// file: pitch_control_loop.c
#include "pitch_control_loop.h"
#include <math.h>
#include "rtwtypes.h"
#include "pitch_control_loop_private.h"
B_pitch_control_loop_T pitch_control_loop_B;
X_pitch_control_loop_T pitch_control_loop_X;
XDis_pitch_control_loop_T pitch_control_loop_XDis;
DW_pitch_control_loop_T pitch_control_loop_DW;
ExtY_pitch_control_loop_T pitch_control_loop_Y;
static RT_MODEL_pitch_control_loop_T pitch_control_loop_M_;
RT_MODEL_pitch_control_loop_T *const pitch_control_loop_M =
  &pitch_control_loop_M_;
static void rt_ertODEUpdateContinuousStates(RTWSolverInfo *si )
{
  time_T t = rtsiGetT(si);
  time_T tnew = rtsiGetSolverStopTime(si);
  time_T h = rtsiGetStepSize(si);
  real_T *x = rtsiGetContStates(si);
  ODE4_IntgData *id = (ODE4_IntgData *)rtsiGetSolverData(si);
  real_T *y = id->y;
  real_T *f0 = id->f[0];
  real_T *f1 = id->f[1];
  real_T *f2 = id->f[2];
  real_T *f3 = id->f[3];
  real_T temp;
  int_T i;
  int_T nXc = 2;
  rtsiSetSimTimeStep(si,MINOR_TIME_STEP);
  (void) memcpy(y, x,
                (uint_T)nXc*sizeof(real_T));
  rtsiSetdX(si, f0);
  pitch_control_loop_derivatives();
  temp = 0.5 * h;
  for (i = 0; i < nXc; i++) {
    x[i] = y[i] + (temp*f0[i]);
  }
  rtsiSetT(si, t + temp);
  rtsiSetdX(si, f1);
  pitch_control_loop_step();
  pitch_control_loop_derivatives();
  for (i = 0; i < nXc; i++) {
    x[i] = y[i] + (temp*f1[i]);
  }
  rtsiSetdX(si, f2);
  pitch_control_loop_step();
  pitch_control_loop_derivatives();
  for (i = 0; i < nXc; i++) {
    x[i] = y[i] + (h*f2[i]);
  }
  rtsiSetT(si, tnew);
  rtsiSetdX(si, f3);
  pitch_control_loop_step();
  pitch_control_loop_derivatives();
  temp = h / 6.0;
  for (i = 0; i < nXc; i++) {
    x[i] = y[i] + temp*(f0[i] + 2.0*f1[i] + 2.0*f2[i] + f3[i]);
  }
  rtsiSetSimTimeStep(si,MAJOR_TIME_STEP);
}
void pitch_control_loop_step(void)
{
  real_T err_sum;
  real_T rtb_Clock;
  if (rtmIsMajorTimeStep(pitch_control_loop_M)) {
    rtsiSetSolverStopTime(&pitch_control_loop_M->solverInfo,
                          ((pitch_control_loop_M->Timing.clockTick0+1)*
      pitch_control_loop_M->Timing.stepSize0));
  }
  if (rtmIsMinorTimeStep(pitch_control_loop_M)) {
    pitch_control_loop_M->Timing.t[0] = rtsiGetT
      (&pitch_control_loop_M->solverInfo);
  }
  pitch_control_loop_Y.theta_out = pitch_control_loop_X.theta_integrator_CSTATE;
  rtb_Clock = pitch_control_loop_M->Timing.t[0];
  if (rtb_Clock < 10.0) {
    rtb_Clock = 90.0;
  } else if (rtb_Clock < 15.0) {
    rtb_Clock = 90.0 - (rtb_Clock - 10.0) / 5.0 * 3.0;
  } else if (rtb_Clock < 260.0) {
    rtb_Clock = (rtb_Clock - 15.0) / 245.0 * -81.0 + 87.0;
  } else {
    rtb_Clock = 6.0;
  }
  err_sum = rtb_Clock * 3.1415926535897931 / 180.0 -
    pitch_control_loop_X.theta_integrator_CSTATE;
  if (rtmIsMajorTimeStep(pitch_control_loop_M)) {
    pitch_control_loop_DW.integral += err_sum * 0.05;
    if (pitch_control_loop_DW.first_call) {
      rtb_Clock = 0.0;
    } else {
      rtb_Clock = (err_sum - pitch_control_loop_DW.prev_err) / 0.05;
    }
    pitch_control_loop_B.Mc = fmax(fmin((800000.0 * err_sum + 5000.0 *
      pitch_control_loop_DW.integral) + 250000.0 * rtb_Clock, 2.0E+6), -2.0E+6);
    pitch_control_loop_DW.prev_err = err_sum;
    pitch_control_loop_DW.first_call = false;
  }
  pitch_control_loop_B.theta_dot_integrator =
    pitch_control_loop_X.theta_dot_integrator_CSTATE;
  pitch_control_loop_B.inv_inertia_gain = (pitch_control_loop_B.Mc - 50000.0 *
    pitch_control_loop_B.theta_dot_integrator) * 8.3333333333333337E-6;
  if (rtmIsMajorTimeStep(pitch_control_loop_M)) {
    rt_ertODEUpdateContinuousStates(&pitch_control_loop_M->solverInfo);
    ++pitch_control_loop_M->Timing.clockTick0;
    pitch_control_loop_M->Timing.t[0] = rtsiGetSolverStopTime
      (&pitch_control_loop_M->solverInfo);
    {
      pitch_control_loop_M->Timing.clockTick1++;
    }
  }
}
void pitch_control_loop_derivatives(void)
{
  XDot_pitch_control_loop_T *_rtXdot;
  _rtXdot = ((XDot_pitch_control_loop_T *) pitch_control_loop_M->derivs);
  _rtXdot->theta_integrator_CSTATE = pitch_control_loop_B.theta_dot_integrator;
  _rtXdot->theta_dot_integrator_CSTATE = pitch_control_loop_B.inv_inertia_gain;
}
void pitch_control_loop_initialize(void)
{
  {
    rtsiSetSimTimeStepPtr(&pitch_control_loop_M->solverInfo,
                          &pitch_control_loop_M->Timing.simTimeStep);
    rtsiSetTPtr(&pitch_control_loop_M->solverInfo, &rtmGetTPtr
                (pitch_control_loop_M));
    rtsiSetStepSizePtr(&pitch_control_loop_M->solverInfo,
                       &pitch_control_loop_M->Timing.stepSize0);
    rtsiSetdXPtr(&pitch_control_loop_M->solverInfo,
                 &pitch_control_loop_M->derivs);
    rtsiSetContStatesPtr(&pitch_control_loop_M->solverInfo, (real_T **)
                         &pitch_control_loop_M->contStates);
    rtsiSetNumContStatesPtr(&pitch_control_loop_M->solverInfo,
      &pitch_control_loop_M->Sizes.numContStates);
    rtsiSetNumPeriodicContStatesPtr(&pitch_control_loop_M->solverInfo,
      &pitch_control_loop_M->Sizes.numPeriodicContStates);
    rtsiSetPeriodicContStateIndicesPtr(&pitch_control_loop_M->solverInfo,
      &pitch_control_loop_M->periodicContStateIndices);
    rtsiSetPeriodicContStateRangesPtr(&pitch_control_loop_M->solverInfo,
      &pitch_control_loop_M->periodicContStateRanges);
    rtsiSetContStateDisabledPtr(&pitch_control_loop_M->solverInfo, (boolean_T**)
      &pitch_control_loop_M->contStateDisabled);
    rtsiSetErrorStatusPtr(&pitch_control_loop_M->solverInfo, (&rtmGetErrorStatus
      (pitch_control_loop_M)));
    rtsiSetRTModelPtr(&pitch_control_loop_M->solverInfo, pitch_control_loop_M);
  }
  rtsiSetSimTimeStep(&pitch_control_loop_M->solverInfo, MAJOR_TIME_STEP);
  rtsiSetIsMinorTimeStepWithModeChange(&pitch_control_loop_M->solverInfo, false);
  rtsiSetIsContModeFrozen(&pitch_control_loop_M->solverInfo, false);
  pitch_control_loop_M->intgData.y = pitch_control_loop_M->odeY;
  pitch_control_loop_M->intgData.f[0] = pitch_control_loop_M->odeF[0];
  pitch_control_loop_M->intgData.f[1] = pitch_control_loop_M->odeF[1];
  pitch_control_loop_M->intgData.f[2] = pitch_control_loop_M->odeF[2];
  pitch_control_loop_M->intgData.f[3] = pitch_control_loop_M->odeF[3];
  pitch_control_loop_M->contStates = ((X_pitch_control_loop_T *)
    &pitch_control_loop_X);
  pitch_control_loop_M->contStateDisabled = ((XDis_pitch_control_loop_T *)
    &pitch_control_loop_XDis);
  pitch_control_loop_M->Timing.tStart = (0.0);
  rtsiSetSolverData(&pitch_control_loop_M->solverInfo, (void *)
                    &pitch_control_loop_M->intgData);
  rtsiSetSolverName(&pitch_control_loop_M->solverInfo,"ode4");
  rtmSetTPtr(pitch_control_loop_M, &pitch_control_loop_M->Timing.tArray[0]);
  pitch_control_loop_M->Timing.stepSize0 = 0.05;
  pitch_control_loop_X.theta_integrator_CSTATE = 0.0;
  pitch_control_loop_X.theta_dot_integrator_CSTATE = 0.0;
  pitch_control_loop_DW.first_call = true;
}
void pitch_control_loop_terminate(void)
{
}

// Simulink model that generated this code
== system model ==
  theta_out : Outport  <- 1: theta_integrator
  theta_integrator : Integrator  <- 1: theta_dot_integrator
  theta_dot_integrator : Integrator  <- 1: inv_inertia_gain
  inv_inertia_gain : Gain  Gain=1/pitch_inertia  <- 1: Sum#1
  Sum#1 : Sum  Inputs=+-  <- 1: MATLABFunction#1, 2: Gain#1
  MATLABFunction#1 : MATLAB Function  <- 1: ZeroOrderHold#1
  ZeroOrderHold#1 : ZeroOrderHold  <- 1: err_sum
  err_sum : Sum  Inputs=+-  <- 1: MATLABFunction#2, 2: theta_integrator
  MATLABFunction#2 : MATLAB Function  <- 1: Clock
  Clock : Clock
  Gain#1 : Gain  Gain=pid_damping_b  <- 1: theta_dot_integrator
== matlab function MATLABFunction#2 ==
function theta_cmd = pitch_program_block(t)
% Embedded Coder-compatible port of src/guidance/pitch_program.m.
% Constants inlined (MATLAB Function blocks do not accept struct
% inputs from config/*.m directly without extra setup); keep in
% sync with config/simulation_settings.m ss.pitch fields by hand,
% documented in docs/01_design_decisions.md.
t_vertical = 10.0; t_kick_end = 15.0; kick_deg = 3.0;
t_pitch_end = 260.0; theta_final_deg = 6.0;
if t < t_vertical
    theta_cmd_deg = 90.0;
elseif t < t_kick_end
    frac = (t - t_vertical) / (t_kick_end - t_vertical);
    theta_cmd_deg = 90.0 - kick_deg * frac;
else
    theta_kick = 90.0 - kick_deg;
    if t < t_pitch_end
        frac = (t - t_kick_end) / (t_pitch_end - t_kick_end);
        theta_cmd_deg = theta_kick + (theta_final_deg - theta_kick) * frac;
    else
        theta_cmd_deg = theta_final_deg;
    end
end
theta_cmd = theta_cmd_deg * pi / 180;

== matlab function MATLABFunction#1 ==
function Mc = pid_controller_block(err)
% Embedded Coder-compatible port of src/control/pid_update.m,
% using persistent variables for controller state (the idiomatic
% Simulink/Embedded-Coder pattern) instead of the explicit
% struct-in/struct-out signature used in the plain-MATLAB
% version -- structs crossing a MATLAB Function block boundary
% need extra bus/type setup that is not worth the complexity
% here. Gains are inlined; keep in sync with
% config/vehicle_parameters.m vp.pid by hand.
persistent integral prev_err first_call
if isempty(first_call)
    integral = 0.0; prev_err = 0.0; first_call = true;
end
kp = 800000.0; ki = 5000.0; kd = 250000.0; out_limit = 2.0e6;
dt = 0.05;
integral = integral + err * dt;
if first_call
    deriv = 0.0;
else
    deriv = (err - prev_err) / dt;
end
u_unsat = kp*err + ki*integral + kd*deriv;
Mc = max(min(u_unsat, out_limit), -out_limit);
prev_err = err;
first_call = false;
